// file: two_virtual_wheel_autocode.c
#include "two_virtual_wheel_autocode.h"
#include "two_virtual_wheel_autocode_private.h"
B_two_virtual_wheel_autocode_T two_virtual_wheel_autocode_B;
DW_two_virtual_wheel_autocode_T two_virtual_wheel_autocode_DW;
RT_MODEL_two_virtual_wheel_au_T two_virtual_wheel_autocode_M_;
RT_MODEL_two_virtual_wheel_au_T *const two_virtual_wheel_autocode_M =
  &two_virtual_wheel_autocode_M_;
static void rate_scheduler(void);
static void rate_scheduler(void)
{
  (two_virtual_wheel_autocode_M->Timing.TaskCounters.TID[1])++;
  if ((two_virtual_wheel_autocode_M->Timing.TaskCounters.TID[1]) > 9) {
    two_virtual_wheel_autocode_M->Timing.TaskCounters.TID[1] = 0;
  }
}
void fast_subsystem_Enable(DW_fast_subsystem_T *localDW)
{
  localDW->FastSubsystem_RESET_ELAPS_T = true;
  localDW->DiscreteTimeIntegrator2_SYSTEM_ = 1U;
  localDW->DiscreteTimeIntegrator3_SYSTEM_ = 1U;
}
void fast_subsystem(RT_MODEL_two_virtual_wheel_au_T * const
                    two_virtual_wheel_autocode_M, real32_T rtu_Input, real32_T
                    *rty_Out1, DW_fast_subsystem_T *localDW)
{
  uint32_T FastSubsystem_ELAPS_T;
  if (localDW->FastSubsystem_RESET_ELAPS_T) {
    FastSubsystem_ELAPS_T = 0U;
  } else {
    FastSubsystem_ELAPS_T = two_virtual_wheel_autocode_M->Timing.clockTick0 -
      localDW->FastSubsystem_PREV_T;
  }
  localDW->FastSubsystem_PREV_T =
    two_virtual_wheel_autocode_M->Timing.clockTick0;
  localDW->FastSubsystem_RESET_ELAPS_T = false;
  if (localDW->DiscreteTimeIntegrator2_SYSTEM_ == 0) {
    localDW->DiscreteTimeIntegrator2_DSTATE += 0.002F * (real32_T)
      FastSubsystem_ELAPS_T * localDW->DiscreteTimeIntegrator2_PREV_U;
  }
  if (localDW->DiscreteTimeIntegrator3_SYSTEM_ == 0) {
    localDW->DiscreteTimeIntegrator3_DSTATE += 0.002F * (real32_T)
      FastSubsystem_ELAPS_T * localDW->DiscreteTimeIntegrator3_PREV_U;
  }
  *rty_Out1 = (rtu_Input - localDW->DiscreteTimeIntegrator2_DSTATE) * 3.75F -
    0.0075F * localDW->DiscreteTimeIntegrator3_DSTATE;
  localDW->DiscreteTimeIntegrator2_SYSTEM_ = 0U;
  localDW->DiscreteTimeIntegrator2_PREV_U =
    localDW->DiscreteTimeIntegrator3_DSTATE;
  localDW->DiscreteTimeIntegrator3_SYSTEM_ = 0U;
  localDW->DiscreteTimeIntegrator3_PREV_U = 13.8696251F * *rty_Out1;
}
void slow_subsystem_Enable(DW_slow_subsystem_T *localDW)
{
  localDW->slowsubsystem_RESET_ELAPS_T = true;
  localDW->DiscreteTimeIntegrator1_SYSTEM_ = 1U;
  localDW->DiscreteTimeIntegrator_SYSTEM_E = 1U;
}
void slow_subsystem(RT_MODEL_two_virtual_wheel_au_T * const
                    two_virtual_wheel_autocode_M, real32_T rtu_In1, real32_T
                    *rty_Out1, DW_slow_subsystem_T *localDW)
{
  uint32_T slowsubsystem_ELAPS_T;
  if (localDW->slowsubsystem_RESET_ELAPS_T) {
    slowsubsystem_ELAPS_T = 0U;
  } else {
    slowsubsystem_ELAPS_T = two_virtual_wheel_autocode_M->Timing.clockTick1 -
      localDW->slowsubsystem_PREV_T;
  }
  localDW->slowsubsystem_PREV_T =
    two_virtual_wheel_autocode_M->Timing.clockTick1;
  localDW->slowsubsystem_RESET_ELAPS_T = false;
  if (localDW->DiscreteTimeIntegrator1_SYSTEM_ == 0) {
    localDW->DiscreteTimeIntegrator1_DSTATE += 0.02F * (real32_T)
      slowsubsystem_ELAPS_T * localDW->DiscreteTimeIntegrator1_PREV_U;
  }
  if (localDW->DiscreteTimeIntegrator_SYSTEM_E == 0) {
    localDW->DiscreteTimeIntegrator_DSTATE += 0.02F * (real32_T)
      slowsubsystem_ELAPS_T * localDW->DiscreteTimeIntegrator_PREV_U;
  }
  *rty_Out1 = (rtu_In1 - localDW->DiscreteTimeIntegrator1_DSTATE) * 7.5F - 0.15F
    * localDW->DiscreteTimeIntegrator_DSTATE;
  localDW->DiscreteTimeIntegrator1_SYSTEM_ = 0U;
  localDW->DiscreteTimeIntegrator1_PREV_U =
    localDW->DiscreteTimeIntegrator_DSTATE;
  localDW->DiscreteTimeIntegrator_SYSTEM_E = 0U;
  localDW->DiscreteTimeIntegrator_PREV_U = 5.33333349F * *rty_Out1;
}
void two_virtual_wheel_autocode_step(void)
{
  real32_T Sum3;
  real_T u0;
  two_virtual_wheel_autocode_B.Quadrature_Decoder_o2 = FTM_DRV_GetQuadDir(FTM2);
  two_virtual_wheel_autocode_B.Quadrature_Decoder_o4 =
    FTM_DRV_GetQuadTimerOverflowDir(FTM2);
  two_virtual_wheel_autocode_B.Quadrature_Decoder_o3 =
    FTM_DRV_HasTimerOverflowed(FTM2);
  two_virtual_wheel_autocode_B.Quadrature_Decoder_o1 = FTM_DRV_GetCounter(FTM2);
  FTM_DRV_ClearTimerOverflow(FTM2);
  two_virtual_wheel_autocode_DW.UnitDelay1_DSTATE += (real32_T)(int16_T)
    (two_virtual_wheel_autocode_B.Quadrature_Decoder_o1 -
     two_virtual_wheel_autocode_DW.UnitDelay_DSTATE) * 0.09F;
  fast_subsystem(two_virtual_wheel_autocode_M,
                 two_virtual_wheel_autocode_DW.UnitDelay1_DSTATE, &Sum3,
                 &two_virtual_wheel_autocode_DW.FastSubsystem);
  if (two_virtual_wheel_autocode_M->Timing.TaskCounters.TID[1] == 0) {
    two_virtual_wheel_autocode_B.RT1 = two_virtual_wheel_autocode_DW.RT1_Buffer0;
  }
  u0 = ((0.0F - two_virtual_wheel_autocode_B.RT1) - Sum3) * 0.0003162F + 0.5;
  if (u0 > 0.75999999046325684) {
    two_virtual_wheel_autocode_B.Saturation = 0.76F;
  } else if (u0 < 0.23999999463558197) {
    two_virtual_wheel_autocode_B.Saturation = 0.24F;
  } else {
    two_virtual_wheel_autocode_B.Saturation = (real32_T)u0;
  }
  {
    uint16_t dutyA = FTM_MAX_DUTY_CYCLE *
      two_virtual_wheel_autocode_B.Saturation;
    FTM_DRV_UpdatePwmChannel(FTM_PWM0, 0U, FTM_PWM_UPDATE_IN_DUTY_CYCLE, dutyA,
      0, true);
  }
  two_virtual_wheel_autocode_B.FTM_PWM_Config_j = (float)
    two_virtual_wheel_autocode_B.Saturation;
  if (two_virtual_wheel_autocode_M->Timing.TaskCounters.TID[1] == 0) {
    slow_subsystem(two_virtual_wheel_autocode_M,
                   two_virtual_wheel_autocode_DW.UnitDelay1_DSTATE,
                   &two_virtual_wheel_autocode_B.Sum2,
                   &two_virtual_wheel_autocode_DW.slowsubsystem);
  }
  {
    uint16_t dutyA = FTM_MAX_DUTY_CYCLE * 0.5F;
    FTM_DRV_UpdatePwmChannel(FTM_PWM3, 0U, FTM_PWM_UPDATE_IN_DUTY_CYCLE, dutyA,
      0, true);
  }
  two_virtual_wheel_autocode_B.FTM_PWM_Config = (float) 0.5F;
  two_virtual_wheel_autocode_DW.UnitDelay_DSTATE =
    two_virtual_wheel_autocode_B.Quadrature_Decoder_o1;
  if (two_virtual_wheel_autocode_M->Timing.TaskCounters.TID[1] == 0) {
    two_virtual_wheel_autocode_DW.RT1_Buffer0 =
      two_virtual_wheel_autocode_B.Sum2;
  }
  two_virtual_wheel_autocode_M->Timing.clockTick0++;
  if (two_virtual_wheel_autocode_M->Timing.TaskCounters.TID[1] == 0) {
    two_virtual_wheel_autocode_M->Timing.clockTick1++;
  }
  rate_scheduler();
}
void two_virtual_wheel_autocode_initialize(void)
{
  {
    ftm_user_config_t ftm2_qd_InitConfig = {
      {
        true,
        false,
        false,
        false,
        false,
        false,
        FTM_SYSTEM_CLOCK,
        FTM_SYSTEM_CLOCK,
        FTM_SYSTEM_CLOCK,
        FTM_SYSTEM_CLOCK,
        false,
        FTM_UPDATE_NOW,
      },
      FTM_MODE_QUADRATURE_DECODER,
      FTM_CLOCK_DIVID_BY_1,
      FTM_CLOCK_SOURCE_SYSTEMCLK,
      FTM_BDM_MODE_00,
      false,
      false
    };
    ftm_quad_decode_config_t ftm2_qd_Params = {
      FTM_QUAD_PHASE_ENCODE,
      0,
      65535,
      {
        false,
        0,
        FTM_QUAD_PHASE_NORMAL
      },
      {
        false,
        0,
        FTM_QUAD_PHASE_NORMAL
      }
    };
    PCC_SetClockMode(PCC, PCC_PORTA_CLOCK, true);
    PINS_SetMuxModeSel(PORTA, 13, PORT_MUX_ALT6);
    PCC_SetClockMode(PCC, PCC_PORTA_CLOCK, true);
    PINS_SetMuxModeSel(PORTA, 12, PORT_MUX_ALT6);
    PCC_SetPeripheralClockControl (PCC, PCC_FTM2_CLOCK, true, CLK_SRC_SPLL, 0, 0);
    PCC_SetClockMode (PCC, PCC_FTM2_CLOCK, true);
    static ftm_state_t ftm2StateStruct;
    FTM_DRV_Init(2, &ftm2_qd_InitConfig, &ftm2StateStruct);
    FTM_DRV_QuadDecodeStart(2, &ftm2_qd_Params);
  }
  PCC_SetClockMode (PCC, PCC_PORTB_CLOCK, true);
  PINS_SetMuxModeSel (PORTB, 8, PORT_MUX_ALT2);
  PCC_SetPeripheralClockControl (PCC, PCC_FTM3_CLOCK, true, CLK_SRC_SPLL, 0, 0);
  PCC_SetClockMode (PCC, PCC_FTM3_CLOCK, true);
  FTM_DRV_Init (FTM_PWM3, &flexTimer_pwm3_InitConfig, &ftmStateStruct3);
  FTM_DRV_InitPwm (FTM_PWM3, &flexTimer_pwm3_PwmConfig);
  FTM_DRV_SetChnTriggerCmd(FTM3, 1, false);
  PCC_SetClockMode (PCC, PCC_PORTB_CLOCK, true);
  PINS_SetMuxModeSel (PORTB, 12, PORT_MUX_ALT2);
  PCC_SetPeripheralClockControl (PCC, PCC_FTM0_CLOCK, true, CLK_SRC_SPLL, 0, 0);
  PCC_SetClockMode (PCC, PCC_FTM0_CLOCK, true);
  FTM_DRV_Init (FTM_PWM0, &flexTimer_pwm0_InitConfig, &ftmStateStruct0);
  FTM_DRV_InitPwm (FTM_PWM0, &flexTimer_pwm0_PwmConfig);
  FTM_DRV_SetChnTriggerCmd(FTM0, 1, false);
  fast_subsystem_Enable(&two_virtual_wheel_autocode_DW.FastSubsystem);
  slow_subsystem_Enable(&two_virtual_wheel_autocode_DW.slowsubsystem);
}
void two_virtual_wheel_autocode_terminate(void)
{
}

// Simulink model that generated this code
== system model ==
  Subsystem#1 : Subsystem  <- 1: Sum#1
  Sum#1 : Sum  Inputs=--  <- 1: RT1, 2: FastSubsystem
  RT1 : RateTransition  <- 1: slowsubsystem
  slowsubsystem : Subsystem  <- 1: RT, Trigger: FunctionCallGenerator#1
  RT : RateTransition  <- 1: Sum#2
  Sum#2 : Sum  <- 1: Gain#1, 2: UnitDelay1
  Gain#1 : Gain  Gain=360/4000  <- 1: DataTypeConversion#1
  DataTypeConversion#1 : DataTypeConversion  <- 1: DataTypeConversion#2
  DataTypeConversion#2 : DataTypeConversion  <- 1: Sum#3
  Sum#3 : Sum  Inputs=+-  <- 1: DataTypeConversion#3, 2: UnitDelay
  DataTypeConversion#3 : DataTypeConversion  <- 1: Quadrature_Decoder
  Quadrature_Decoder : mbd_s32k1xx_ec_toolbox/Motor Control Blocks/FTM Blocks/Quadrature_Decoder
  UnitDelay : UnitDelay  <- 1: DataTypeConversion#3
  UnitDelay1 : UnitDelay  <- 1: Sum#2
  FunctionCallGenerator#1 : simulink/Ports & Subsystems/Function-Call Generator
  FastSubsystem : Subsystem  <- 1: Sum#2, Trigger: FunctionCallGenerator#2
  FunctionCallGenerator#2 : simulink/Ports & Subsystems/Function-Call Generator
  FTM_PWM_Config : mbd_s32k1xx_ec_toolbox/Motor Control Blocks/FTM Blocks/FTM_PWM_Config  <- 1: Constant#1
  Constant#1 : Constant  Value=0.5
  MBD_S32K1xx_Config_Information#1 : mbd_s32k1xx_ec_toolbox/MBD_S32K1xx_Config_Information
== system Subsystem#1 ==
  In1 : Inport
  FTM_PWM_Config#1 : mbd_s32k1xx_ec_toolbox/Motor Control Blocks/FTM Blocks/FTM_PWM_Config  <- 1: Saturation
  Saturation : Saturate  UpperLimit=0.76  LowerLimit=0.24  <- 1: Sum#4
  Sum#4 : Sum  <- 1: Gain#2, 2: Constant#2
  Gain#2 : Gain  Gain=0.0003162  <- 1: In1
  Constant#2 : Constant  Value=0.5
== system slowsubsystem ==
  Inport#1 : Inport
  TriggerPort#1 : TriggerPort  TriggerType=function-call
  Out1 : Outport  <- 1: Sum2
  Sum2 : Sum  Inputs=+-  <- 1: Gain#3, 2: Gain#4
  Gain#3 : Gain  Gain=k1  <- 1: Sum#5
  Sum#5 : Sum  Inputs=+-  <- 1: Inport#1, 2: DiscreteTimeIntegrator1
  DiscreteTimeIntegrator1 : DiscreteIntegrator  <- 1: DiscreteTimeIntegrator
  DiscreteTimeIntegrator : DiscreteIntegrator  <- 1: Gain#5
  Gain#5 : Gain  Gain=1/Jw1  <- 1: Sum2
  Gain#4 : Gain  Gain=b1  <- 1: DiscreteTimeIntegrator
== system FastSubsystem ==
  Input : Inport
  TriggerPort#2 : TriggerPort  TriggerType=function-call
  Outport#1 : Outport  <- 1: Sum3
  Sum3 : Sum  Inputs=+-  <- 1: Gain#6, 2: Gain#7
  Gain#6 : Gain  Gain=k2  <- 1: Sum#6
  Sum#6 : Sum  Inputs=+-  <- 1: Input, 2: DiscreteTimeIntegrator2
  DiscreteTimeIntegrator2 : DiscreteIntegrator  <- 1: DiscreteTimeIntegrator3
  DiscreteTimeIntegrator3 : DiscreteIntegrator  <- 1: Gain#8
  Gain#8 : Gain  Gain=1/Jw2  <- 1: Sum3
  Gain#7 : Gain  Gain=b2  <- 1: DiscreteTimeIntegrator3

